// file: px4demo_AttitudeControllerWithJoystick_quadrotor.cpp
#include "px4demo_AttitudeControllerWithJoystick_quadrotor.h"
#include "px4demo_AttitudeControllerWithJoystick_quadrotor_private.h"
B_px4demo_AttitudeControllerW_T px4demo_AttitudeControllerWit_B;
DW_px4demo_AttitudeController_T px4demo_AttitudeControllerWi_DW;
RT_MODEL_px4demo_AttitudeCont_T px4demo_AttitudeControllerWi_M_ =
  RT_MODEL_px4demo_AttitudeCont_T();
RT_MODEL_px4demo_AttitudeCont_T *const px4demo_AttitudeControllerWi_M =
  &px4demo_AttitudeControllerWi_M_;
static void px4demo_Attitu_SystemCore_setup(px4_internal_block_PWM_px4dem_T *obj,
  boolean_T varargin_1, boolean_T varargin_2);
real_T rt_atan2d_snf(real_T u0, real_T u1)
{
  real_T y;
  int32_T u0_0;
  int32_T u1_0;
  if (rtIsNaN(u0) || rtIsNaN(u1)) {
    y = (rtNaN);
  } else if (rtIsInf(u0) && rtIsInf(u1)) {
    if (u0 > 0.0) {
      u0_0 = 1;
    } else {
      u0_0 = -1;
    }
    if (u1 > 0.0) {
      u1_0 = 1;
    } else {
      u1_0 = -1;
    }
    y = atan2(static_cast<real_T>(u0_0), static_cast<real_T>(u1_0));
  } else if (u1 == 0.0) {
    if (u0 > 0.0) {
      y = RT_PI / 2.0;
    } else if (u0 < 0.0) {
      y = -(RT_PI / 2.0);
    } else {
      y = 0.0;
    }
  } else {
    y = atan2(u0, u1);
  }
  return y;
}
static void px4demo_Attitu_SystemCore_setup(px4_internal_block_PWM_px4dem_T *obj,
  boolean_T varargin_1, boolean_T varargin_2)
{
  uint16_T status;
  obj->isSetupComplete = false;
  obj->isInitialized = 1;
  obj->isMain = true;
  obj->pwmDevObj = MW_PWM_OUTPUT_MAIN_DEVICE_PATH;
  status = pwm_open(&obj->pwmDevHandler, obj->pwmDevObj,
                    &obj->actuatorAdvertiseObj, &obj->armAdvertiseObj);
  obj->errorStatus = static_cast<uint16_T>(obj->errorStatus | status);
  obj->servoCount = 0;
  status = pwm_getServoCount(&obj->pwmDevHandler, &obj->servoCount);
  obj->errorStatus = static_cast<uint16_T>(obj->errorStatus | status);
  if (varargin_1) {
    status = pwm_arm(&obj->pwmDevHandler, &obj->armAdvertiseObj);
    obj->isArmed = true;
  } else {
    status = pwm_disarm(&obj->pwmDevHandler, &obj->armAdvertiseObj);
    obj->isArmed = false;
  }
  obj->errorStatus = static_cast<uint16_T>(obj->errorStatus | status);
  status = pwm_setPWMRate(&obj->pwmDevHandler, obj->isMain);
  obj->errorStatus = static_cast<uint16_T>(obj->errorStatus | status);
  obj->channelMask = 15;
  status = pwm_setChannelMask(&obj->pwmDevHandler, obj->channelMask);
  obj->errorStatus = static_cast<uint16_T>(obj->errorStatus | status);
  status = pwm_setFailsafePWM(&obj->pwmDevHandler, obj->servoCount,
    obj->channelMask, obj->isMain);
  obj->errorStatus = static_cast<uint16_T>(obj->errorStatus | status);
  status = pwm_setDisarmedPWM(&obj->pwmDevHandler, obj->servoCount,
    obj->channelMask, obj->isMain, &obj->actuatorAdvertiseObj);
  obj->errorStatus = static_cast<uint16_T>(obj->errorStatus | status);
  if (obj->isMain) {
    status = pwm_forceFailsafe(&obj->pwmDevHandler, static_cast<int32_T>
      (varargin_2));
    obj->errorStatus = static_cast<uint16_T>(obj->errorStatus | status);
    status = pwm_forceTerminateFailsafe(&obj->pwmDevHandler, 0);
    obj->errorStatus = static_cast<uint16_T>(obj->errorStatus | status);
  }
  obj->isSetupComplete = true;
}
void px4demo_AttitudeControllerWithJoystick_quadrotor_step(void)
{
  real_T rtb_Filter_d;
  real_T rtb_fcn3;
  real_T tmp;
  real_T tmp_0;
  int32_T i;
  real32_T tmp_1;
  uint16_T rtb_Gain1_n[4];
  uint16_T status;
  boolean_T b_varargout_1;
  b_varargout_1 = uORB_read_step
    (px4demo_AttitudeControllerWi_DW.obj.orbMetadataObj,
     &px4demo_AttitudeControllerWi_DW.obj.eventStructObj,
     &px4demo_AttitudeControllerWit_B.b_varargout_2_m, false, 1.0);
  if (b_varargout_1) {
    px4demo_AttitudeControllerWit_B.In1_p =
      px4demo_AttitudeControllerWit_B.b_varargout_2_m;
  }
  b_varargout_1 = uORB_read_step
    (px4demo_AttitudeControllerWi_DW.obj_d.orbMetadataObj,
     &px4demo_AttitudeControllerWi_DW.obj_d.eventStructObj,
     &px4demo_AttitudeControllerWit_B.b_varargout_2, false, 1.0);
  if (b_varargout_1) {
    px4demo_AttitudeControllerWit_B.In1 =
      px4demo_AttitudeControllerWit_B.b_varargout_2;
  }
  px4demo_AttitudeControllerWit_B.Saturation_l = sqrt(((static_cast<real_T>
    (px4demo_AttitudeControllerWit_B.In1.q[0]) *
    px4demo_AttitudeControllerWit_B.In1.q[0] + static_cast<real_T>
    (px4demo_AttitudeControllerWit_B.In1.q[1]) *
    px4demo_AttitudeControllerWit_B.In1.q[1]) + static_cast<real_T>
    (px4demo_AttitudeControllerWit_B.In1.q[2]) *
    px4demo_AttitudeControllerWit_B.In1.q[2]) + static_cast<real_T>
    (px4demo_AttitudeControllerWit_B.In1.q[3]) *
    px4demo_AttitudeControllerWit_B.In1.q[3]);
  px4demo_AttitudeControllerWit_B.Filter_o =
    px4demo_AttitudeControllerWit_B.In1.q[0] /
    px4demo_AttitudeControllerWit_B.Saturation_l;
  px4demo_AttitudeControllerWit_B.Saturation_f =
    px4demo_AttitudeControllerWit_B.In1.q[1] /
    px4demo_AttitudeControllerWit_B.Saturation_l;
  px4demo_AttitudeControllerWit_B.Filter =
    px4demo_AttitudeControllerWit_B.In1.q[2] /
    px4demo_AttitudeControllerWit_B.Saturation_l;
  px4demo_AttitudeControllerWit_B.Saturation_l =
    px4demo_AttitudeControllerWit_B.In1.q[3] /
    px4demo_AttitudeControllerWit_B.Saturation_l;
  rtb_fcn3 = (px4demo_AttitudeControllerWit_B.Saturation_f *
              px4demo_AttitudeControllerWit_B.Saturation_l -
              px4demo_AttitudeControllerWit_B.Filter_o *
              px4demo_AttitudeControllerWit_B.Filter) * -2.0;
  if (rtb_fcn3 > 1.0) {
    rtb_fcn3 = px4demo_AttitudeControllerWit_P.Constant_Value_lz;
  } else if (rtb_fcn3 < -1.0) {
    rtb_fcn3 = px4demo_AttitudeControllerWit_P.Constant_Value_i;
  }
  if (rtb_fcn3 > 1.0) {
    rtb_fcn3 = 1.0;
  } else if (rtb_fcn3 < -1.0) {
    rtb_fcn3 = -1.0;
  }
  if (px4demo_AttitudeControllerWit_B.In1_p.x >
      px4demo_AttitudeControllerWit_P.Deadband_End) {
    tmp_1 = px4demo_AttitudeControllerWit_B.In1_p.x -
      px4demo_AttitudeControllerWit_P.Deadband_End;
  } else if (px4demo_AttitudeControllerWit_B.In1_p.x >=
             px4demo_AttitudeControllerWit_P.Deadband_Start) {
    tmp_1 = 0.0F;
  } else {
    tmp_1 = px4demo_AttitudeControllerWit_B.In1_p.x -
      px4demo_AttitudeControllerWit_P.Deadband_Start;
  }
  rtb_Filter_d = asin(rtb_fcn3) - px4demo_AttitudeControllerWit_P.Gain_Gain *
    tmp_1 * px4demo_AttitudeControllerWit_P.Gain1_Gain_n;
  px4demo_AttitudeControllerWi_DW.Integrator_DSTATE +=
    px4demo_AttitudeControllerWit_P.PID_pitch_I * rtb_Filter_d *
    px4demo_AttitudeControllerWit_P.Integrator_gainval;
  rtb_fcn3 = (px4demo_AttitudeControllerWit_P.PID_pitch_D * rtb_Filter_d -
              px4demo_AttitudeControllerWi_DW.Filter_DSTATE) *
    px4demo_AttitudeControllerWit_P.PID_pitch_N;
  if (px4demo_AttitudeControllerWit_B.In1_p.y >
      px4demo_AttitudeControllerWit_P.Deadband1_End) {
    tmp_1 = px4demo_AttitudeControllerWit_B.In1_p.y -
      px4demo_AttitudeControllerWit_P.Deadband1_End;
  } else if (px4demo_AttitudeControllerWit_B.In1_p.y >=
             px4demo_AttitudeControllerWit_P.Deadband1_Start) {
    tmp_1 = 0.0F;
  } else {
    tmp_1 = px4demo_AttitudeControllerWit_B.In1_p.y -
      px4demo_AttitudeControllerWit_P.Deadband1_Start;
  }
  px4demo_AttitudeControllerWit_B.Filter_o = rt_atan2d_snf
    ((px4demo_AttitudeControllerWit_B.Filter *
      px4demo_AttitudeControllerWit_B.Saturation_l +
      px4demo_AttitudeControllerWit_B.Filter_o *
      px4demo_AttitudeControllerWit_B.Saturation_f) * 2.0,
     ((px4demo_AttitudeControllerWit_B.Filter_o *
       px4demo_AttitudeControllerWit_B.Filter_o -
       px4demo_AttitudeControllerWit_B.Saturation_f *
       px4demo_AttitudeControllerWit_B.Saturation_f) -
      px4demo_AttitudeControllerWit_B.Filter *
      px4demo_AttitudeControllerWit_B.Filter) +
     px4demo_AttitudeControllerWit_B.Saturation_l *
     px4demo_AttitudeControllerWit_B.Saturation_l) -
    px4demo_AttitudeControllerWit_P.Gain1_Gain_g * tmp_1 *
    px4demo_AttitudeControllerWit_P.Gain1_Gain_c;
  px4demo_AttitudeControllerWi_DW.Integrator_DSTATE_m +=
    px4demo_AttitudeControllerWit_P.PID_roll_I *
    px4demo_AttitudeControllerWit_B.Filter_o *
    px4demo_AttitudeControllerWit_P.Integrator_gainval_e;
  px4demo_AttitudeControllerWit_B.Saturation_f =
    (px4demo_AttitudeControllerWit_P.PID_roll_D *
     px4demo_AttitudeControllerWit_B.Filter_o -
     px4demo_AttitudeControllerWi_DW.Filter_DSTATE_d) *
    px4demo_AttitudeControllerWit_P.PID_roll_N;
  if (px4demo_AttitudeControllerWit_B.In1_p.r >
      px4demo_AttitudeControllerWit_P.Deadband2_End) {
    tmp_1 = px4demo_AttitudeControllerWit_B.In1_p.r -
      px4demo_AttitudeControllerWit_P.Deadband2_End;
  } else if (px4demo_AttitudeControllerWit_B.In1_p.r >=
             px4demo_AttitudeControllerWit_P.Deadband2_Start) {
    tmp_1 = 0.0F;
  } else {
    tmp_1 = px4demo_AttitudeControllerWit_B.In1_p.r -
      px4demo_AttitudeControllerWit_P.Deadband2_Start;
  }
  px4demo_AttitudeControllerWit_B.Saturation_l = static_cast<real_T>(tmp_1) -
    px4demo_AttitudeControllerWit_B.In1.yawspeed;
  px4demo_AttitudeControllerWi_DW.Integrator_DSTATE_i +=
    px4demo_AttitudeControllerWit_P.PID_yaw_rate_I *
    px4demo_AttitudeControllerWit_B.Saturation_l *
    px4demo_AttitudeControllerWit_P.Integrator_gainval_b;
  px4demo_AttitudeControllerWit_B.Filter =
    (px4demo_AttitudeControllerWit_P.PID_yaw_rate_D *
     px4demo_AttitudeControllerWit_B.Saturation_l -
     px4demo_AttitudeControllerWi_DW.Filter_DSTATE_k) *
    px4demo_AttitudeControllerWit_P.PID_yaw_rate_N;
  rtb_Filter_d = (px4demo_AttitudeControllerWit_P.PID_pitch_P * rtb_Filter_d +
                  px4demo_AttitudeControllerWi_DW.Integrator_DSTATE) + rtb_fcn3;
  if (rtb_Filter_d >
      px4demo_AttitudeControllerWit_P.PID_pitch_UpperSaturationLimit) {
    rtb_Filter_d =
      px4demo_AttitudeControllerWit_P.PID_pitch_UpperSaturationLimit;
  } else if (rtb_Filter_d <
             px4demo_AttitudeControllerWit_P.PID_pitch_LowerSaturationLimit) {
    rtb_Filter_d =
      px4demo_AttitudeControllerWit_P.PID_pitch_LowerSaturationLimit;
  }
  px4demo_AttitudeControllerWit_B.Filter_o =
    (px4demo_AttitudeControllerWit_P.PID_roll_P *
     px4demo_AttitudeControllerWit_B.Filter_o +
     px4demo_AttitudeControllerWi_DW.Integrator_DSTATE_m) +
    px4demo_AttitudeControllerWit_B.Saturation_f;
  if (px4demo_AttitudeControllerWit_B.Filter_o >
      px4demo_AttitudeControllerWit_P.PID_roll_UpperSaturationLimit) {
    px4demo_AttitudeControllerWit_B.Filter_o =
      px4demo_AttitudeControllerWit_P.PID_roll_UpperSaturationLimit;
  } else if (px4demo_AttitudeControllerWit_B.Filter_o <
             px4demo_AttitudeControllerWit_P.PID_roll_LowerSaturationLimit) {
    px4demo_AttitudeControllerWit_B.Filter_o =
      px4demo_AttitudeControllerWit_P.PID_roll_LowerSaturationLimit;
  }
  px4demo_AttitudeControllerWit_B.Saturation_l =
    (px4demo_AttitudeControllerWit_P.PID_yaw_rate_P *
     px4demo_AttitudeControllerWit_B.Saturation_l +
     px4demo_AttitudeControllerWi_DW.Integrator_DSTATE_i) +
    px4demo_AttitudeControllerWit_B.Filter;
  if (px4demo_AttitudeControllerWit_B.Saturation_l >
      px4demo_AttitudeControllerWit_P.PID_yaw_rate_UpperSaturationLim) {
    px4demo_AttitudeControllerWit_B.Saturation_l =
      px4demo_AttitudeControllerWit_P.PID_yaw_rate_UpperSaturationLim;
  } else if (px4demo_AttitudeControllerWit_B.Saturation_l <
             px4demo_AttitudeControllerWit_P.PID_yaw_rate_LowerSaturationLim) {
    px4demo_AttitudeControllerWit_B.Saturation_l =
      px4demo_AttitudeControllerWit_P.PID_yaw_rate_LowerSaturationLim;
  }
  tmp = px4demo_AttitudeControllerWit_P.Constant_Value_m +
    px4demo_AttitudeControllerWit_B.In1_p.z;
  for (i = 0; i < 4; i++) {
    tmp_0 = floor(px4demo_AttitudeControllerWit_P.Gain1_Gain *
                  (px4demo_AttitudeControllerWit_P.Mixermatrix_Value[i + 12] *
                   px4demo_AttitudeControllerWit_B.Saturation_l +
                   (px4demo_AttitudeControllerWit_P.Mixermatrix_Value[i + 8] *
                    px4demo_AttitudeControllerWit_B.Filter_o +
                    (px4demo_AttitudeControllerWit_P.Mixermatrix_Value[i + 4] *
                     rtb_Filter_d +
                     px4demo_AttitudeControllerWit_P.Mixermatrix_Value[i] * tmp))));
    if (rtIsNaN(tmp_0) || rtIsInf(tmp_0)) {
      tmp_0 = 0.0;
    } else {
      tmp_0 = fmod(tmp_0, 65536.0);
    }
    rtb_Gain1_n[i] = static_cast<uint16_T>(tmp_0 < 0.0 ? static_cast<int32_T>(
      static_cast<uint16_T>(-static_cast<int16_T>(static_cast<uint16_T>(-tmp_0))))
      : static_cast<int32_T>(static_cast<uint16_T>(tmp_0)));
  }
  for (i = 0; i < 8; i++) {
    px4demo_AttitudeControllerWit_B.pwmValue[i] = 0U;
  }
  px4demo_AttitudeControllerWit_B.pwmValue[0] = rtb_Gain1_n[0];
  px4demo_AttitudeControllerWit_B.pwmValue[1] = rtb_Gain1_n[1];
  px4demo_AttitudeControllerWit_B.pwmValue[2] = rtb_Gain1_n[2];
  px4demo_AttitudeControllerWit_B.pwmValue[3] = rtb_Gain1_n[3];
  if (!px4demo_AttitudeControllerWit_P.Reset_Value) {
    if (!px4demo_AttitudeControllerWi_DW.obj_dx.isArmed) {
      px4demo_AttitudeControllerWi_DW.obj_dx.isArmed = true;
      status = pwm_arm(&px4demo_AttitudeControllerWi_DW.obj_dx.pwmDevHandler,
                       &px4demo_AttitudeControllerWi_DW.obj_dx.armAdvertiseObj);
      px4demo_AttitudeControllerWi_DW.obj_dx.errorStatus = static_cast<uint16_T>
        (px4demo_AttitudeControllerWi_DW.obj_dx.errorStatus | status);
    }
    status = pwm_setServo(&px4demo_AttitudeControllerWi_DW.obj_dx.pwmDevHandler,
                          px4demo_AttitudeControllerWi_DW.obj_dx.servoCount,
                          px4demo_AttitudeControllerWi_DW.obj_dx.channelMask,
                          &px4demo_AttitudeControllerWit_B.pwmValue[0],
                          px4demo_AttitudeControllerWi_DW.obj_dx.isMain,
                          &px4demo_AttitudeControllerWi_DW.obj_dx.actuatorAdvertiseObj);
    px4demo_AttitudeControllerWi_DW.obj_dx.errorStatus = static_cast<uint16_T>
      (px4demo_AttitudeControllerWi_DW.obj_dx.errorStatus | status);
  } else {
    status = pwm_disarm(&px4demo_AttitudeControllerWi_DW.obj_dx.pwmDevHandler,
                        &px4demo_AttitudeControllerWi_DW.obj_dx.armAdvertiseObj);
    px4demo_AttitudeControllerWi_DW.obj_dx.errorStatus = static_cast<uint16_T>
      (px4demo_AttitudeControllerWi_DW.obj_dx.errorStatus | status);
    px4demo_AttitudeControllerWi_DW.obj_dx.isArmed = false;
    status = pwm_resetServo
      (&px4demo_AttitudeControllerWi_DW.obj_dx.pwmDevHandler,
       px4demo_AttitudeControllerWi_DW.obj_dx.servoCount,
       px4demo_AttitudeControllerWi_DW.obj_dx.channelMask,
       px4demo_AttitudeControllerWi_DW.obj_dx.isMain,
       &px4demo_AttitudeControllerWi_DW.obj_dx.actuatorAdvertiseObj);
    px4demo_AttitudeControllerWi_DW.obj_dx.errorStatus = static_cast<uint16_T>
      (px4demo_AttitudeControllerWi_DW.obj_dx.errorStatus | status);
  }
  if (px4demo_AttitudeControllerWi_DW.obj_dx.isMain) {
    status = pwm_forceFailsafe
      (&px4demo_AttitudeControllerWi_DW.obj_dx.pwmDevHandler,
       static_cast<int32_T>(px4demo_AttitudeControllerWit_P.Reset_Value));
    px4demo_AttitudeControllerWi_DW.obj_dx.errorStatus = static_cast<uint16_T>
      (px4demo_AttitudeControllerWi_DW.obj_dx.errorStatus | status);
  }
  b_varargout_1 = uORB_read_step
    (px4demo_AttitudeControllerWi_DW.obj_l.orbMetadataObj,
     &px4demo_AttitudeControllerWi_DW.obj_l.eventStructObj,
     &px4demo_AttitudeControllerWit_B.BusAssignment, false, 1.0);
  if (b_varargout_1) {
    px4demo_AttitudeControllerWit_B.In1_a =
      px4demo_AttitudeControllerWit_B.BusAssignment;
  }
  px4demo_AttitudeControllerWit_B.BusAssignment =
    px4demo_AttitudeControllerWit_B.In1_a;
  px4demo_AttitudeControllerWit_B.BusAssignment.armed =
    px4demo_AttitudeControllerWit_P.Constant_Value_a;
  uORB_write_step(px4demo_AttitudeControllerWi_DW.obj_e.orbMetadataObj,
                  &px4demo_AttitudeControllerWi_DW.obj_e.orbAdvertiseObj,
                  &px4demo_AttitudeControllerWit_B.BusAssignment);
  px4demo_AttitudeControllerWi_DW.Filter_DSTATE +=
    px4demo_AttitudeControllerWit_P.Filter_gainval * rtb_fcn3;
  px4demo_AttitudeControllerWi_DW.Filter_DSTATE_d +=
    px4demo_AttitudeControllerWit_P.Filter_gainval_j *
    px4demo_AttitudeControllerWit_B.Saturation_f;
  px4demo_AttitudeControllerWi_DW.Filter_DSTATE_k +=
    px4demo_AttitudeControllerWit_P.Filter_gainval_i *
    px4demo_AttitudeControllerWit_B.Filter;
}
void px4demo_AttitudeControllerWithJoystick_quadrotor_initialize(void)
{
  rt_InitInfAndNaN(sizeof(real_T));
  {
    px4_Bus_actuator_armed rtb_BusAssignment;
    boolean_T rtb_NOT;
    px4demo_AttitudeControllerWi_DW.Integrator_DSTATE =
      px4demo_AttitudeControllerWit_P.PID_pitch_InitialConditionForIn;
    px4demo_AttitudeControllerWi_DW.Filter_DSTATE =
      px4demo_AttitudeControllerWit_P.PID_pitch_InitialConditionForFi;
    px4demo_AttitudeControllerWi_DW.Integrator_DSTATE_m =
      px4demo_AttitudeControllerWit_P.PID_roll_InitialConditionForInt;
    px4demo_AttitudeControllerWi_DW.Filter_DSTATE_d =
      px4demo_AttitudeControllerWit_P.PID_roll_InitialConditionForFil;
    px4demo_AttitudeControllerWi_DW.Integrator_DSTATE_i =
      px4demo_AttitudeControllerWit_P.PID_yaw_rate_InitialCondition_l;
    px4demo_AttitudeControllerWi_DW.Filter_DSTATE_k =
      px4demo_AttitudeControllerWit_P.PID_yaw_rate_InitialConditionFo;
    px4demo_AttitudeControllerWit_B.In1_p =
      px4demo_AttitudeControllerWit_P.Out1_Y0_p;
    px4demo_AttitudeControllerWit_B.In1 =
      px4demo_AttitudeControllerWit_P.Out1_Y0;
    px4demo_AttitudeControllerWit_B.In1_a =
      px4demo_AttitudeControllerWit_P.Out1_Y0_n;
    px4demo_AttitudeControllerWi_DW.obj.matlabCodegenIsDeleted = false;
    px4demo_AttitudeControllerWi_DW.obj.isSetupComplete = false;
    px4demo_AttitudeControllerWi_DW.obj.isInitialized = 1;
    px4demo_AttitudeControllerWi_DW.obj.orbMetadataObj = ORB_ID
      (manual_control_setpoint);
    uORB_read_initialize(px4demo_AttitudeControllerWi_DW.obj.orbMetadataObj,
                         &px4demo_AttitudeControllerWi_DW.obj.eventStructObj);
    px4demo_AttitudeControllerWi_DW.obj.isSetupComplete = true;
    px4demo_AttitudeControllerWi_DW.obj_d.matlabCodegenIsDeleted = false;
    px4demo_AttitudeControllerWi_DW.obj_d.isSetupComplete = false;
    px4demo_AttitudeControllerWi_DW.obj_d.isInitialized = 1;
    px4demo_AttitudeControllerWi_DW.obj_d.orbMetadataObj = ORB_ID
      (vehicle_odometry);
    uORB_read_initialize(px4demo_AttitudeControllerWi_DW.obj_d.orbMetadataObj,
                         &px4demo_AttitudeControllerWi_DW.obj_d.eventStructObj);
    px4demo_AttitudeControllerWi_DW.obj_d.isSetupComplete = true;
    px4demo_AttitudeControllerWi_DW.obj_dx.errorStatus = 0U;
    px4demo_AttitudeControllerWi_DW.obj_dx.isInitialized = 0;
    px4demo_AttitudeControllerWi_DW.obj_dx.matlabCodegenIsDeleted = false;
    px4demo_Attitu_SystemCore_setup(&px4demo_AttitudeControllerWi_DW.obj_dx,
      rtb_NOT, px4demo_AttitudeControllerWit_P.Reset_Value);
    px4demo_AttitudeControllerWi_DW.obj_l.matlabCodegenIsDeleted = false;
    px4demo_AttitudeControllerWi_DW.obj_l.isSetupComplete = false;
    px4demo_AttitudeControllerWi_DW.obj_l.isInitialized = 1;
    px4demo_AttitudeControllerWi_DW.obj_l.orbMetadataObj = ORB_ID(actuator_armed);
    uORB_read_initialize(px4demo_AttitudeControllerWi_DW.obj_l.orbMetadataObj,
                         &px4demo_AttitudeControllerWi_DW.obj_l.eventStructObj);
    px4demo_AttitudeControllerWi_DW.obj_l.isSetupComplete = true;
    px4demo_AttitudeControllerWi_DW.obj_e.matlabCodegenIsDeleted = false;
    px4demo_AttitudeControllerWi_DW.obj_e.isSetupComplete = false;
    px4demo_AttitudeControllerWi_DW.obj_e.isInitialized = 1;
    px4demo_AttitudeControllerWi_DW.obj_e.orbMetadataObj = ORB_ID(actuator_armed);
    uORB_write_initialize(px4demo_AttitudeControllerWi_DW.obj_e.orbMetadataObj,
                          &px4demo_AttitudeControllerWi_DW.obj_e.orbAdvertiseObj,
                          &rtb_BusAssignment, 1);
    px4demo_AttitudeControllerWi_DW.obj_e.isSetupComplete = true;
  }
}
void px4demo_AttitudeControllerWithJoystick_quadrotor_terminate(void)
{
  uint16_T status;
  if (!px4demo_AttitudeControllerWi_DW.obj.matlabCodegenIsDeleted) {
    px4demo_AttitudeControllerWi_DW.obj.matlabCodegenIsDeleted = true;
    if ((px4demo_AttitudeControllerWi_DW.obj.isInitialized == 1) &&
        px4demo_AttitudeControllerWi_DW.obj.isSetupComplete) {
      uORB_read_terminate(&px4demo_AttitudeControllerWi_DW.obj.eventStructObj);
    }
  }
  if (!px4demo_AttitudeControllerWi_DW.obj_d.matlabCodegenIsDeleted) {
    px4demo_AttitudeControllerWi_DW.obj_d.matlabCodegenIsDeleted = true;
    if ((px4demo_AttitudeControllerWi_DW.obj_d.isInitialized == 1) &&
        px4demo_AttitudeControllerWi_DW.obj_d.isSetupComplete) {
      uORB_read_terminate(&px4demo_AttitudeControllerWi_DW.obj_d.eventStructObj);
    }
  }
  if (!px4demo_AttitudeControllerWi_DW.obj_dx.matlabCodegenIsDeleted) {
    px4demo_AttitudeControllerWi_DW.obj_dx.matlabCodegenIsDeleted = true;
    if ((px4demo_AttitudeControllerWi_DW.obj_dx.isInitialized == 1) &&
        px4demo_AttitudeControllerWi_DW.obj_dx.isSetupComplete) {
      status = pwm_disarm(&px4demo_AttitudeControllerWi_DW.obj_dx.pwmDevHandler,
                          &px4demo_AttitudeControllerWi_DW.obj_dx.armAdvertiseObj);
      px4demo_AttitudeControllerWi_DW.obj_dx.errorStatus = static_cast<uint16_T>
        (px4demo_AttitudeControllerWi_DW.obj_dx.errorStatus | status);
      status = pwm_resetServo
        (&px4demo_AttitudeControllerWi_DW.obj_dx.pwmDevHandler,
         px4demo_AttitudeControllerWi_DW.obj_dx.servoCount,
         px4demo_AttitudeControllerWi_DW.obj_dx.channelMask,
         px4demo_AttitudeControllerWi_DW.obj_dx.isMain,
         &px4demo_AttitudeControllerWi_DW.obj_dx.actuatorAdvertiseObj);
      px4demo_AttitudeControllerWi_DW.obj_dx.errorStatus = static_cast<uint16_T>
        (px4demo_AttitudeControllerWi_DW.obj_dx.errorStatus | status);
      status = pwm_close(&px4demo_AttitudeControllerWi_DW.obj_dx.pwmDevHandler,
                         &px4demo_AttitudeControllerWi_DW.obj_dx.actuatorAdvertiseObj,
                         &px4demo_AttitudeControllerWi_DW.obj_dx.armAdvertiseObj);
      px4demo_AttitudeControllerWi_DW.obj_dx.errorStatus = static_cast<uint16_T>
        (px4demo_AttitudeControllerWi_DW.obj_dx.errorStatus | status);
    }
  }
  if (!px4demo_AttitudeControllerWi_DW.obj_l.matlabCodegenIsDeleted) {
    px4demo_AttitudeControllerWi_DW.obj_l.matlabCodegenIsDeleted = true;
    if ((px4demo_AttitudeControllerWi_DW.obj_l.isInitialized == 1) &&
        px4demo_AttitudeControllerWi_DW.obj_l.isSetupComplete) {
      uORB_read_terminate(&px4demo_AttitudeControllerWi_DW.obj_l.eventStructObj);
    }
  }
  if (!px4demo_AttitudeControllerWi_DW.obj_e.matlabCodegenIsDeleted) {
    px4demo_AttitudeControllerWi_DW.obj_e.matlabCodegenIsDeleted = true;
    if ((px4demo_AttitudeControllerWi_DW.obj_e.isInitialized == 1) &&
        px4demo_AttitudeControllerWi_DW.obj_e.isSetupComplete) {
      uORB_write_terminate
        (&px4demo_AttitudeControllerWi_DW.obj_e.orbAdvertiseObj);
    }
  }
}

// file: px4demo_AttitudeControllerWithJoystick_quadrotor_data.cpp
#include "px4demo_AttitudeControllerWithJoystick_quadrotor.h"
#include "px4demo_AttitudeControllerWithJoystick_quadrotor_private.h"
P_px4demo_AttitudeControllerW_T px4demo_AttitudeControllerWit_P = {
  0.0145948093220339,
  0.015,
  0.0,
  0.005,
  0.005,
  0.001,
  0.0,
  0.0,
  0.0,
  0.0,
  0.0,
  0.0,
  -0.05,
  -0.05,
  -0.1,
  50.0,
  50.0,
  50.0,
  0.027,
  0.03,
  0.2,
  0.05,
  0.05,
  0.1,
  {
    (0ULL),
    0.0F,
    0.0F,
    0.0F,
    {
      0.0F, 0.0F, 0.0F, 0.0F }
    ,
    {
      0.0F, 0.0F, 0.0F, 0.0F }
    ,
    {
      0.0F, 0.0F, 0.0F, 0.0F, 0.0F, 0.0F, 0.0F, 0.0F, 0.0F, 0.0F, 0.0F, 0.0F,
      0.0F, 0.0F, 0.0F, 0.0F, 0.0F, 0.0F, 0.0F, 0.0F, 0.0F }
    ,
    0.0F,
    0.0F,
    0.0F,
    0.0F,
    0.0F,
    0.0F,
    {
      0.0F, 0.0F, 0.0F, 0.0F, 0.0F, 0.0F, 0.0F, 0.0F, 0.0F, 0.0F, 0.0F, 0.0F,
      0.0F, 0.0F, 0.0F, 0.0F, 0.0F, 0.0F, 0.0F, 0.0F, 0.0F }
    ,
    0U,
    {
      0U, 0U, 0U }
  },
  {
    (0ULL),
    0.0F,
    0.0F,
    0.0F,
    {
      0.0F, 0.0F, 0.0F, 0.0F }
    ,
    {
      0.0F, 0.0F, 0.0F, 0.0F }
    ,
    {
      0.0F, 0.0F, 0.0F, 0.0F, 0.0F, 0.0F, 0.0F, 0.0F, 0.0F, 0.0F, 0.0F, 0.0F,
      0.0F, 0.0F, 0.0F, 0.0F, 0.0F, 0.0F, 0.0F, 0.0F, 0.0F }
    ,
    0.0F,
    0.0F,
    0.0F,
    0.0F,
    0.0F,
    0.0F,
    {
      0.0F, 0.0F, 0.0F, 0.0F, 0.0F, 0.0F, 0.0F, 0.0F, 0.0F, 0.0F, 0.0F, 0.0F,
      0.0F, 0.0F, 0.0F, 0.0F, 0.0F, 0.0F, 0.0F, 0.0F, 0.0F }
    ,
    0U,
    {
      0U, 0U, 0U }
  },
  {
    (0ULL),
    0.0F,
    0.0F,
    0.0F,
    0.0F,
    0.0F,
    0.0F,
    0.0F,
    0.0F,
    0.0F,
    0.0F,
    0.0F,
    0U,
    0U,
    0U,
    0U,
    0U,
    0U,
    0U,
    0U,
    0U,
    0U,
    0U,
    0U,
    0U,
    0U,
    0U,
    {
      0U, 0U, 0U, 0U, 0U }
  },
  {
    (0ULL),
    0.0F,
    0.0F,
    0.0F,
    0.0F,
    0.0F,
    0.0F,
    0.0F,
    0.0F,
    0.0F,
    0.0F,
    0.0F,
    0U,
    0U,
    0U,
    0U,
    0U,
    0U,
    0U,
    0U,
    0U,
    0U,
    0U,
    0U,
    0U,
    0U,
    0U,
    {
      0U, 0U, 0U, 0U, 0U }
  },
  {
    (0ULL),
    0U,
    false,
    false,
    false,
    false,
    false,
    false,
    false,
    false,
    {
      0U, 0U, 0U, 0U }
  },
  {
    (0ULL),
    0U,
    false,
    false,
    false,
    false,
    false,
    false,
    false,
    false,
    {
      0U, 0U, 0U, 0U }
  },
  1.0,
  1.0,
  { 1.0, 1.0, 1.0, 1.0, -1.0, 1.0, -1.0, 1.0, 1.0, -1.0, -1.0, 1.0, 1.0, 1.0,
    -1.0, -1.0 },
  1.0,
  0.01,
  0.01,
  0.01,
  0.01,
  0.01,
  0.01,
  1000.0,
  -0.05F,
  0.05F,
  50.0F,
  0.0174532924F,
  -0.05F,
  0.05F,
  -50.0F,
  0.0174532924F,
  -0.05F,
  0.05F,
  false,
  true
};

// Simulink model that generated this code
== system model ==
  PX4PWMOutput#1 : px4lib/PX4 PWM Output  <- 1: NOT, 2: Reset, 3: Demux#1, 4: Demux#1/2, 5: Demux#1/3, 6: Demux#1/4
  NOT : Logic  Operator=NOT  <- 1: Reset
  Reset : Constant  Value=0
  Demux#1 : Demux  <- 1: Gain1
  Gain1 : Gain  Gain=1000  <- 1: Product#1
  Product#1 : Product  Multiplication=Matrix(*)  <- 1: Mixermatrix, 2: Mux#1
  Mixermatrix : Constant  Value=[1 -1 1 1;1 1 -1 1;1 -1 -1 -1;1 1 1 -1]
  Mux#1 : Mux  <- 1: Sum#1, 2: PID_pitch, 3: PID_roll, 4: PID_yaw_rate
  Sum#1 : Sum  <- 1: Constant, 2: BusSelector#1
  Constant : Constant
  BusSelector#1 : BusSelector  <- 1: PX4uORBRead#1/2
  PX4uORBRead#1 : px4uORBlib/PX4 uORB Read
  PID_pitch : pid_lib/PID Controller  Controller=PID  Form=Parallel  TimeDomain=Discrete-time  IntegratorMethod=Backward Euler  P=0.027  I=0.005  D=0.0145948093220339  N=50  InitialConditionForIntegrator=0  ExternalReset=none  LimitOutput=on  UpperSaturationLimit=0.05  LowerSaturationLimit=-0.05  <- 1: Sum#2
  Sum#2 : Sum  Inputs=+-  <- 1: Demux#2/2, 2: DegreestoRadians#1
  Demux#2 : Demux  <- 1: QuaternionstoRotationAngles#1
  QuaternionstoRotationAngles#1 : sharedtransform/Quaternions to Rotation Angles  <- 1: DataTypeConversion#1
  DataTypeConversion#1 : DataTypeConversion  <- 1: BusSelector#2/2
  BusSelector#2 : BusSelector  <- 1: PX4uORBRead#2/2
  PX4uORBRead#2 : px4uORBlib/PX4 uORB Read
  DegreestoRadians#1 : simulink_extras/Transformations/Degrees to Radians  <- 1: Gain
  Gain : Gain  Gain=50  <- 1: Deadband
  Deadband : DeadZone  LowerValue=-0.05  UpperValue=0.05  <- 1: BusSelector#1/2
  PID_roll : pid_lib/PID Controller  Controller=PID  Form=Parallel  TimeDomain=Discrete-time  IntegratorMethod=Backward Euler  P=0.03  I=0.005  D=0.015  N=50  InitialConditionForIntegrator=0  ExternalReset=none  LimitOutput=on  UpperSaturationLimit=0.05  LowerSaturationLimit=-0.05  <- 1: Sum#3
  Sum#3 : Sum  Inputs=+-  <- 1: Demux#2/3, 2: DegreestoRadians#2
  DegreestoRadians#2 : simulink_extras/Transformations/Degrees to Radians  <- 1: Gain#1
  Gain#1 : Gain  Gain=-50  <- 1: Deadband1
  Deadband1 : DeadZone  LowerValue=-0.05  UpperValue=0.05  <- 1: BusSelector#1/3
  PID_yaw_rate : pid_lib/PID Controller  Controller=PID  Form=Parallel  TimeDomain=Discrete-time  IntegratorMethod=Backward Euler  P=0.2  I=0.001  D=0  N=50  InitialConditionForIntegrator=0  ExternalReset=none  LimitOutput=on  UpperSaturationLimit=0.1  LowerSaturationLimit=-0.1  <- 1: Sum#4
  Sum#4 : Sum  Inputs=+-  <- 1: Deadband2, 2: DataTypeConversion#2
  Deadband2 : DeadZone  LowerValue=-0.05  UpperValue=0.05  <- 1: BusSelector#1/4
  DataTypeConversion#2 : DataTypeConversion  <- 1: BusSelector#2
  PX4uORBWrite#1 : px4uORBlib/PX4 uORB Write  <- 1: BusAssignment
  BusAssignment : BusAssignment  <- 1: PX4uORBRead#3/2, 2: Constant#1
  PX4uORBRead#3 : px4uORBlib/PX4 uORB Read
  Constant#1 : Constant
